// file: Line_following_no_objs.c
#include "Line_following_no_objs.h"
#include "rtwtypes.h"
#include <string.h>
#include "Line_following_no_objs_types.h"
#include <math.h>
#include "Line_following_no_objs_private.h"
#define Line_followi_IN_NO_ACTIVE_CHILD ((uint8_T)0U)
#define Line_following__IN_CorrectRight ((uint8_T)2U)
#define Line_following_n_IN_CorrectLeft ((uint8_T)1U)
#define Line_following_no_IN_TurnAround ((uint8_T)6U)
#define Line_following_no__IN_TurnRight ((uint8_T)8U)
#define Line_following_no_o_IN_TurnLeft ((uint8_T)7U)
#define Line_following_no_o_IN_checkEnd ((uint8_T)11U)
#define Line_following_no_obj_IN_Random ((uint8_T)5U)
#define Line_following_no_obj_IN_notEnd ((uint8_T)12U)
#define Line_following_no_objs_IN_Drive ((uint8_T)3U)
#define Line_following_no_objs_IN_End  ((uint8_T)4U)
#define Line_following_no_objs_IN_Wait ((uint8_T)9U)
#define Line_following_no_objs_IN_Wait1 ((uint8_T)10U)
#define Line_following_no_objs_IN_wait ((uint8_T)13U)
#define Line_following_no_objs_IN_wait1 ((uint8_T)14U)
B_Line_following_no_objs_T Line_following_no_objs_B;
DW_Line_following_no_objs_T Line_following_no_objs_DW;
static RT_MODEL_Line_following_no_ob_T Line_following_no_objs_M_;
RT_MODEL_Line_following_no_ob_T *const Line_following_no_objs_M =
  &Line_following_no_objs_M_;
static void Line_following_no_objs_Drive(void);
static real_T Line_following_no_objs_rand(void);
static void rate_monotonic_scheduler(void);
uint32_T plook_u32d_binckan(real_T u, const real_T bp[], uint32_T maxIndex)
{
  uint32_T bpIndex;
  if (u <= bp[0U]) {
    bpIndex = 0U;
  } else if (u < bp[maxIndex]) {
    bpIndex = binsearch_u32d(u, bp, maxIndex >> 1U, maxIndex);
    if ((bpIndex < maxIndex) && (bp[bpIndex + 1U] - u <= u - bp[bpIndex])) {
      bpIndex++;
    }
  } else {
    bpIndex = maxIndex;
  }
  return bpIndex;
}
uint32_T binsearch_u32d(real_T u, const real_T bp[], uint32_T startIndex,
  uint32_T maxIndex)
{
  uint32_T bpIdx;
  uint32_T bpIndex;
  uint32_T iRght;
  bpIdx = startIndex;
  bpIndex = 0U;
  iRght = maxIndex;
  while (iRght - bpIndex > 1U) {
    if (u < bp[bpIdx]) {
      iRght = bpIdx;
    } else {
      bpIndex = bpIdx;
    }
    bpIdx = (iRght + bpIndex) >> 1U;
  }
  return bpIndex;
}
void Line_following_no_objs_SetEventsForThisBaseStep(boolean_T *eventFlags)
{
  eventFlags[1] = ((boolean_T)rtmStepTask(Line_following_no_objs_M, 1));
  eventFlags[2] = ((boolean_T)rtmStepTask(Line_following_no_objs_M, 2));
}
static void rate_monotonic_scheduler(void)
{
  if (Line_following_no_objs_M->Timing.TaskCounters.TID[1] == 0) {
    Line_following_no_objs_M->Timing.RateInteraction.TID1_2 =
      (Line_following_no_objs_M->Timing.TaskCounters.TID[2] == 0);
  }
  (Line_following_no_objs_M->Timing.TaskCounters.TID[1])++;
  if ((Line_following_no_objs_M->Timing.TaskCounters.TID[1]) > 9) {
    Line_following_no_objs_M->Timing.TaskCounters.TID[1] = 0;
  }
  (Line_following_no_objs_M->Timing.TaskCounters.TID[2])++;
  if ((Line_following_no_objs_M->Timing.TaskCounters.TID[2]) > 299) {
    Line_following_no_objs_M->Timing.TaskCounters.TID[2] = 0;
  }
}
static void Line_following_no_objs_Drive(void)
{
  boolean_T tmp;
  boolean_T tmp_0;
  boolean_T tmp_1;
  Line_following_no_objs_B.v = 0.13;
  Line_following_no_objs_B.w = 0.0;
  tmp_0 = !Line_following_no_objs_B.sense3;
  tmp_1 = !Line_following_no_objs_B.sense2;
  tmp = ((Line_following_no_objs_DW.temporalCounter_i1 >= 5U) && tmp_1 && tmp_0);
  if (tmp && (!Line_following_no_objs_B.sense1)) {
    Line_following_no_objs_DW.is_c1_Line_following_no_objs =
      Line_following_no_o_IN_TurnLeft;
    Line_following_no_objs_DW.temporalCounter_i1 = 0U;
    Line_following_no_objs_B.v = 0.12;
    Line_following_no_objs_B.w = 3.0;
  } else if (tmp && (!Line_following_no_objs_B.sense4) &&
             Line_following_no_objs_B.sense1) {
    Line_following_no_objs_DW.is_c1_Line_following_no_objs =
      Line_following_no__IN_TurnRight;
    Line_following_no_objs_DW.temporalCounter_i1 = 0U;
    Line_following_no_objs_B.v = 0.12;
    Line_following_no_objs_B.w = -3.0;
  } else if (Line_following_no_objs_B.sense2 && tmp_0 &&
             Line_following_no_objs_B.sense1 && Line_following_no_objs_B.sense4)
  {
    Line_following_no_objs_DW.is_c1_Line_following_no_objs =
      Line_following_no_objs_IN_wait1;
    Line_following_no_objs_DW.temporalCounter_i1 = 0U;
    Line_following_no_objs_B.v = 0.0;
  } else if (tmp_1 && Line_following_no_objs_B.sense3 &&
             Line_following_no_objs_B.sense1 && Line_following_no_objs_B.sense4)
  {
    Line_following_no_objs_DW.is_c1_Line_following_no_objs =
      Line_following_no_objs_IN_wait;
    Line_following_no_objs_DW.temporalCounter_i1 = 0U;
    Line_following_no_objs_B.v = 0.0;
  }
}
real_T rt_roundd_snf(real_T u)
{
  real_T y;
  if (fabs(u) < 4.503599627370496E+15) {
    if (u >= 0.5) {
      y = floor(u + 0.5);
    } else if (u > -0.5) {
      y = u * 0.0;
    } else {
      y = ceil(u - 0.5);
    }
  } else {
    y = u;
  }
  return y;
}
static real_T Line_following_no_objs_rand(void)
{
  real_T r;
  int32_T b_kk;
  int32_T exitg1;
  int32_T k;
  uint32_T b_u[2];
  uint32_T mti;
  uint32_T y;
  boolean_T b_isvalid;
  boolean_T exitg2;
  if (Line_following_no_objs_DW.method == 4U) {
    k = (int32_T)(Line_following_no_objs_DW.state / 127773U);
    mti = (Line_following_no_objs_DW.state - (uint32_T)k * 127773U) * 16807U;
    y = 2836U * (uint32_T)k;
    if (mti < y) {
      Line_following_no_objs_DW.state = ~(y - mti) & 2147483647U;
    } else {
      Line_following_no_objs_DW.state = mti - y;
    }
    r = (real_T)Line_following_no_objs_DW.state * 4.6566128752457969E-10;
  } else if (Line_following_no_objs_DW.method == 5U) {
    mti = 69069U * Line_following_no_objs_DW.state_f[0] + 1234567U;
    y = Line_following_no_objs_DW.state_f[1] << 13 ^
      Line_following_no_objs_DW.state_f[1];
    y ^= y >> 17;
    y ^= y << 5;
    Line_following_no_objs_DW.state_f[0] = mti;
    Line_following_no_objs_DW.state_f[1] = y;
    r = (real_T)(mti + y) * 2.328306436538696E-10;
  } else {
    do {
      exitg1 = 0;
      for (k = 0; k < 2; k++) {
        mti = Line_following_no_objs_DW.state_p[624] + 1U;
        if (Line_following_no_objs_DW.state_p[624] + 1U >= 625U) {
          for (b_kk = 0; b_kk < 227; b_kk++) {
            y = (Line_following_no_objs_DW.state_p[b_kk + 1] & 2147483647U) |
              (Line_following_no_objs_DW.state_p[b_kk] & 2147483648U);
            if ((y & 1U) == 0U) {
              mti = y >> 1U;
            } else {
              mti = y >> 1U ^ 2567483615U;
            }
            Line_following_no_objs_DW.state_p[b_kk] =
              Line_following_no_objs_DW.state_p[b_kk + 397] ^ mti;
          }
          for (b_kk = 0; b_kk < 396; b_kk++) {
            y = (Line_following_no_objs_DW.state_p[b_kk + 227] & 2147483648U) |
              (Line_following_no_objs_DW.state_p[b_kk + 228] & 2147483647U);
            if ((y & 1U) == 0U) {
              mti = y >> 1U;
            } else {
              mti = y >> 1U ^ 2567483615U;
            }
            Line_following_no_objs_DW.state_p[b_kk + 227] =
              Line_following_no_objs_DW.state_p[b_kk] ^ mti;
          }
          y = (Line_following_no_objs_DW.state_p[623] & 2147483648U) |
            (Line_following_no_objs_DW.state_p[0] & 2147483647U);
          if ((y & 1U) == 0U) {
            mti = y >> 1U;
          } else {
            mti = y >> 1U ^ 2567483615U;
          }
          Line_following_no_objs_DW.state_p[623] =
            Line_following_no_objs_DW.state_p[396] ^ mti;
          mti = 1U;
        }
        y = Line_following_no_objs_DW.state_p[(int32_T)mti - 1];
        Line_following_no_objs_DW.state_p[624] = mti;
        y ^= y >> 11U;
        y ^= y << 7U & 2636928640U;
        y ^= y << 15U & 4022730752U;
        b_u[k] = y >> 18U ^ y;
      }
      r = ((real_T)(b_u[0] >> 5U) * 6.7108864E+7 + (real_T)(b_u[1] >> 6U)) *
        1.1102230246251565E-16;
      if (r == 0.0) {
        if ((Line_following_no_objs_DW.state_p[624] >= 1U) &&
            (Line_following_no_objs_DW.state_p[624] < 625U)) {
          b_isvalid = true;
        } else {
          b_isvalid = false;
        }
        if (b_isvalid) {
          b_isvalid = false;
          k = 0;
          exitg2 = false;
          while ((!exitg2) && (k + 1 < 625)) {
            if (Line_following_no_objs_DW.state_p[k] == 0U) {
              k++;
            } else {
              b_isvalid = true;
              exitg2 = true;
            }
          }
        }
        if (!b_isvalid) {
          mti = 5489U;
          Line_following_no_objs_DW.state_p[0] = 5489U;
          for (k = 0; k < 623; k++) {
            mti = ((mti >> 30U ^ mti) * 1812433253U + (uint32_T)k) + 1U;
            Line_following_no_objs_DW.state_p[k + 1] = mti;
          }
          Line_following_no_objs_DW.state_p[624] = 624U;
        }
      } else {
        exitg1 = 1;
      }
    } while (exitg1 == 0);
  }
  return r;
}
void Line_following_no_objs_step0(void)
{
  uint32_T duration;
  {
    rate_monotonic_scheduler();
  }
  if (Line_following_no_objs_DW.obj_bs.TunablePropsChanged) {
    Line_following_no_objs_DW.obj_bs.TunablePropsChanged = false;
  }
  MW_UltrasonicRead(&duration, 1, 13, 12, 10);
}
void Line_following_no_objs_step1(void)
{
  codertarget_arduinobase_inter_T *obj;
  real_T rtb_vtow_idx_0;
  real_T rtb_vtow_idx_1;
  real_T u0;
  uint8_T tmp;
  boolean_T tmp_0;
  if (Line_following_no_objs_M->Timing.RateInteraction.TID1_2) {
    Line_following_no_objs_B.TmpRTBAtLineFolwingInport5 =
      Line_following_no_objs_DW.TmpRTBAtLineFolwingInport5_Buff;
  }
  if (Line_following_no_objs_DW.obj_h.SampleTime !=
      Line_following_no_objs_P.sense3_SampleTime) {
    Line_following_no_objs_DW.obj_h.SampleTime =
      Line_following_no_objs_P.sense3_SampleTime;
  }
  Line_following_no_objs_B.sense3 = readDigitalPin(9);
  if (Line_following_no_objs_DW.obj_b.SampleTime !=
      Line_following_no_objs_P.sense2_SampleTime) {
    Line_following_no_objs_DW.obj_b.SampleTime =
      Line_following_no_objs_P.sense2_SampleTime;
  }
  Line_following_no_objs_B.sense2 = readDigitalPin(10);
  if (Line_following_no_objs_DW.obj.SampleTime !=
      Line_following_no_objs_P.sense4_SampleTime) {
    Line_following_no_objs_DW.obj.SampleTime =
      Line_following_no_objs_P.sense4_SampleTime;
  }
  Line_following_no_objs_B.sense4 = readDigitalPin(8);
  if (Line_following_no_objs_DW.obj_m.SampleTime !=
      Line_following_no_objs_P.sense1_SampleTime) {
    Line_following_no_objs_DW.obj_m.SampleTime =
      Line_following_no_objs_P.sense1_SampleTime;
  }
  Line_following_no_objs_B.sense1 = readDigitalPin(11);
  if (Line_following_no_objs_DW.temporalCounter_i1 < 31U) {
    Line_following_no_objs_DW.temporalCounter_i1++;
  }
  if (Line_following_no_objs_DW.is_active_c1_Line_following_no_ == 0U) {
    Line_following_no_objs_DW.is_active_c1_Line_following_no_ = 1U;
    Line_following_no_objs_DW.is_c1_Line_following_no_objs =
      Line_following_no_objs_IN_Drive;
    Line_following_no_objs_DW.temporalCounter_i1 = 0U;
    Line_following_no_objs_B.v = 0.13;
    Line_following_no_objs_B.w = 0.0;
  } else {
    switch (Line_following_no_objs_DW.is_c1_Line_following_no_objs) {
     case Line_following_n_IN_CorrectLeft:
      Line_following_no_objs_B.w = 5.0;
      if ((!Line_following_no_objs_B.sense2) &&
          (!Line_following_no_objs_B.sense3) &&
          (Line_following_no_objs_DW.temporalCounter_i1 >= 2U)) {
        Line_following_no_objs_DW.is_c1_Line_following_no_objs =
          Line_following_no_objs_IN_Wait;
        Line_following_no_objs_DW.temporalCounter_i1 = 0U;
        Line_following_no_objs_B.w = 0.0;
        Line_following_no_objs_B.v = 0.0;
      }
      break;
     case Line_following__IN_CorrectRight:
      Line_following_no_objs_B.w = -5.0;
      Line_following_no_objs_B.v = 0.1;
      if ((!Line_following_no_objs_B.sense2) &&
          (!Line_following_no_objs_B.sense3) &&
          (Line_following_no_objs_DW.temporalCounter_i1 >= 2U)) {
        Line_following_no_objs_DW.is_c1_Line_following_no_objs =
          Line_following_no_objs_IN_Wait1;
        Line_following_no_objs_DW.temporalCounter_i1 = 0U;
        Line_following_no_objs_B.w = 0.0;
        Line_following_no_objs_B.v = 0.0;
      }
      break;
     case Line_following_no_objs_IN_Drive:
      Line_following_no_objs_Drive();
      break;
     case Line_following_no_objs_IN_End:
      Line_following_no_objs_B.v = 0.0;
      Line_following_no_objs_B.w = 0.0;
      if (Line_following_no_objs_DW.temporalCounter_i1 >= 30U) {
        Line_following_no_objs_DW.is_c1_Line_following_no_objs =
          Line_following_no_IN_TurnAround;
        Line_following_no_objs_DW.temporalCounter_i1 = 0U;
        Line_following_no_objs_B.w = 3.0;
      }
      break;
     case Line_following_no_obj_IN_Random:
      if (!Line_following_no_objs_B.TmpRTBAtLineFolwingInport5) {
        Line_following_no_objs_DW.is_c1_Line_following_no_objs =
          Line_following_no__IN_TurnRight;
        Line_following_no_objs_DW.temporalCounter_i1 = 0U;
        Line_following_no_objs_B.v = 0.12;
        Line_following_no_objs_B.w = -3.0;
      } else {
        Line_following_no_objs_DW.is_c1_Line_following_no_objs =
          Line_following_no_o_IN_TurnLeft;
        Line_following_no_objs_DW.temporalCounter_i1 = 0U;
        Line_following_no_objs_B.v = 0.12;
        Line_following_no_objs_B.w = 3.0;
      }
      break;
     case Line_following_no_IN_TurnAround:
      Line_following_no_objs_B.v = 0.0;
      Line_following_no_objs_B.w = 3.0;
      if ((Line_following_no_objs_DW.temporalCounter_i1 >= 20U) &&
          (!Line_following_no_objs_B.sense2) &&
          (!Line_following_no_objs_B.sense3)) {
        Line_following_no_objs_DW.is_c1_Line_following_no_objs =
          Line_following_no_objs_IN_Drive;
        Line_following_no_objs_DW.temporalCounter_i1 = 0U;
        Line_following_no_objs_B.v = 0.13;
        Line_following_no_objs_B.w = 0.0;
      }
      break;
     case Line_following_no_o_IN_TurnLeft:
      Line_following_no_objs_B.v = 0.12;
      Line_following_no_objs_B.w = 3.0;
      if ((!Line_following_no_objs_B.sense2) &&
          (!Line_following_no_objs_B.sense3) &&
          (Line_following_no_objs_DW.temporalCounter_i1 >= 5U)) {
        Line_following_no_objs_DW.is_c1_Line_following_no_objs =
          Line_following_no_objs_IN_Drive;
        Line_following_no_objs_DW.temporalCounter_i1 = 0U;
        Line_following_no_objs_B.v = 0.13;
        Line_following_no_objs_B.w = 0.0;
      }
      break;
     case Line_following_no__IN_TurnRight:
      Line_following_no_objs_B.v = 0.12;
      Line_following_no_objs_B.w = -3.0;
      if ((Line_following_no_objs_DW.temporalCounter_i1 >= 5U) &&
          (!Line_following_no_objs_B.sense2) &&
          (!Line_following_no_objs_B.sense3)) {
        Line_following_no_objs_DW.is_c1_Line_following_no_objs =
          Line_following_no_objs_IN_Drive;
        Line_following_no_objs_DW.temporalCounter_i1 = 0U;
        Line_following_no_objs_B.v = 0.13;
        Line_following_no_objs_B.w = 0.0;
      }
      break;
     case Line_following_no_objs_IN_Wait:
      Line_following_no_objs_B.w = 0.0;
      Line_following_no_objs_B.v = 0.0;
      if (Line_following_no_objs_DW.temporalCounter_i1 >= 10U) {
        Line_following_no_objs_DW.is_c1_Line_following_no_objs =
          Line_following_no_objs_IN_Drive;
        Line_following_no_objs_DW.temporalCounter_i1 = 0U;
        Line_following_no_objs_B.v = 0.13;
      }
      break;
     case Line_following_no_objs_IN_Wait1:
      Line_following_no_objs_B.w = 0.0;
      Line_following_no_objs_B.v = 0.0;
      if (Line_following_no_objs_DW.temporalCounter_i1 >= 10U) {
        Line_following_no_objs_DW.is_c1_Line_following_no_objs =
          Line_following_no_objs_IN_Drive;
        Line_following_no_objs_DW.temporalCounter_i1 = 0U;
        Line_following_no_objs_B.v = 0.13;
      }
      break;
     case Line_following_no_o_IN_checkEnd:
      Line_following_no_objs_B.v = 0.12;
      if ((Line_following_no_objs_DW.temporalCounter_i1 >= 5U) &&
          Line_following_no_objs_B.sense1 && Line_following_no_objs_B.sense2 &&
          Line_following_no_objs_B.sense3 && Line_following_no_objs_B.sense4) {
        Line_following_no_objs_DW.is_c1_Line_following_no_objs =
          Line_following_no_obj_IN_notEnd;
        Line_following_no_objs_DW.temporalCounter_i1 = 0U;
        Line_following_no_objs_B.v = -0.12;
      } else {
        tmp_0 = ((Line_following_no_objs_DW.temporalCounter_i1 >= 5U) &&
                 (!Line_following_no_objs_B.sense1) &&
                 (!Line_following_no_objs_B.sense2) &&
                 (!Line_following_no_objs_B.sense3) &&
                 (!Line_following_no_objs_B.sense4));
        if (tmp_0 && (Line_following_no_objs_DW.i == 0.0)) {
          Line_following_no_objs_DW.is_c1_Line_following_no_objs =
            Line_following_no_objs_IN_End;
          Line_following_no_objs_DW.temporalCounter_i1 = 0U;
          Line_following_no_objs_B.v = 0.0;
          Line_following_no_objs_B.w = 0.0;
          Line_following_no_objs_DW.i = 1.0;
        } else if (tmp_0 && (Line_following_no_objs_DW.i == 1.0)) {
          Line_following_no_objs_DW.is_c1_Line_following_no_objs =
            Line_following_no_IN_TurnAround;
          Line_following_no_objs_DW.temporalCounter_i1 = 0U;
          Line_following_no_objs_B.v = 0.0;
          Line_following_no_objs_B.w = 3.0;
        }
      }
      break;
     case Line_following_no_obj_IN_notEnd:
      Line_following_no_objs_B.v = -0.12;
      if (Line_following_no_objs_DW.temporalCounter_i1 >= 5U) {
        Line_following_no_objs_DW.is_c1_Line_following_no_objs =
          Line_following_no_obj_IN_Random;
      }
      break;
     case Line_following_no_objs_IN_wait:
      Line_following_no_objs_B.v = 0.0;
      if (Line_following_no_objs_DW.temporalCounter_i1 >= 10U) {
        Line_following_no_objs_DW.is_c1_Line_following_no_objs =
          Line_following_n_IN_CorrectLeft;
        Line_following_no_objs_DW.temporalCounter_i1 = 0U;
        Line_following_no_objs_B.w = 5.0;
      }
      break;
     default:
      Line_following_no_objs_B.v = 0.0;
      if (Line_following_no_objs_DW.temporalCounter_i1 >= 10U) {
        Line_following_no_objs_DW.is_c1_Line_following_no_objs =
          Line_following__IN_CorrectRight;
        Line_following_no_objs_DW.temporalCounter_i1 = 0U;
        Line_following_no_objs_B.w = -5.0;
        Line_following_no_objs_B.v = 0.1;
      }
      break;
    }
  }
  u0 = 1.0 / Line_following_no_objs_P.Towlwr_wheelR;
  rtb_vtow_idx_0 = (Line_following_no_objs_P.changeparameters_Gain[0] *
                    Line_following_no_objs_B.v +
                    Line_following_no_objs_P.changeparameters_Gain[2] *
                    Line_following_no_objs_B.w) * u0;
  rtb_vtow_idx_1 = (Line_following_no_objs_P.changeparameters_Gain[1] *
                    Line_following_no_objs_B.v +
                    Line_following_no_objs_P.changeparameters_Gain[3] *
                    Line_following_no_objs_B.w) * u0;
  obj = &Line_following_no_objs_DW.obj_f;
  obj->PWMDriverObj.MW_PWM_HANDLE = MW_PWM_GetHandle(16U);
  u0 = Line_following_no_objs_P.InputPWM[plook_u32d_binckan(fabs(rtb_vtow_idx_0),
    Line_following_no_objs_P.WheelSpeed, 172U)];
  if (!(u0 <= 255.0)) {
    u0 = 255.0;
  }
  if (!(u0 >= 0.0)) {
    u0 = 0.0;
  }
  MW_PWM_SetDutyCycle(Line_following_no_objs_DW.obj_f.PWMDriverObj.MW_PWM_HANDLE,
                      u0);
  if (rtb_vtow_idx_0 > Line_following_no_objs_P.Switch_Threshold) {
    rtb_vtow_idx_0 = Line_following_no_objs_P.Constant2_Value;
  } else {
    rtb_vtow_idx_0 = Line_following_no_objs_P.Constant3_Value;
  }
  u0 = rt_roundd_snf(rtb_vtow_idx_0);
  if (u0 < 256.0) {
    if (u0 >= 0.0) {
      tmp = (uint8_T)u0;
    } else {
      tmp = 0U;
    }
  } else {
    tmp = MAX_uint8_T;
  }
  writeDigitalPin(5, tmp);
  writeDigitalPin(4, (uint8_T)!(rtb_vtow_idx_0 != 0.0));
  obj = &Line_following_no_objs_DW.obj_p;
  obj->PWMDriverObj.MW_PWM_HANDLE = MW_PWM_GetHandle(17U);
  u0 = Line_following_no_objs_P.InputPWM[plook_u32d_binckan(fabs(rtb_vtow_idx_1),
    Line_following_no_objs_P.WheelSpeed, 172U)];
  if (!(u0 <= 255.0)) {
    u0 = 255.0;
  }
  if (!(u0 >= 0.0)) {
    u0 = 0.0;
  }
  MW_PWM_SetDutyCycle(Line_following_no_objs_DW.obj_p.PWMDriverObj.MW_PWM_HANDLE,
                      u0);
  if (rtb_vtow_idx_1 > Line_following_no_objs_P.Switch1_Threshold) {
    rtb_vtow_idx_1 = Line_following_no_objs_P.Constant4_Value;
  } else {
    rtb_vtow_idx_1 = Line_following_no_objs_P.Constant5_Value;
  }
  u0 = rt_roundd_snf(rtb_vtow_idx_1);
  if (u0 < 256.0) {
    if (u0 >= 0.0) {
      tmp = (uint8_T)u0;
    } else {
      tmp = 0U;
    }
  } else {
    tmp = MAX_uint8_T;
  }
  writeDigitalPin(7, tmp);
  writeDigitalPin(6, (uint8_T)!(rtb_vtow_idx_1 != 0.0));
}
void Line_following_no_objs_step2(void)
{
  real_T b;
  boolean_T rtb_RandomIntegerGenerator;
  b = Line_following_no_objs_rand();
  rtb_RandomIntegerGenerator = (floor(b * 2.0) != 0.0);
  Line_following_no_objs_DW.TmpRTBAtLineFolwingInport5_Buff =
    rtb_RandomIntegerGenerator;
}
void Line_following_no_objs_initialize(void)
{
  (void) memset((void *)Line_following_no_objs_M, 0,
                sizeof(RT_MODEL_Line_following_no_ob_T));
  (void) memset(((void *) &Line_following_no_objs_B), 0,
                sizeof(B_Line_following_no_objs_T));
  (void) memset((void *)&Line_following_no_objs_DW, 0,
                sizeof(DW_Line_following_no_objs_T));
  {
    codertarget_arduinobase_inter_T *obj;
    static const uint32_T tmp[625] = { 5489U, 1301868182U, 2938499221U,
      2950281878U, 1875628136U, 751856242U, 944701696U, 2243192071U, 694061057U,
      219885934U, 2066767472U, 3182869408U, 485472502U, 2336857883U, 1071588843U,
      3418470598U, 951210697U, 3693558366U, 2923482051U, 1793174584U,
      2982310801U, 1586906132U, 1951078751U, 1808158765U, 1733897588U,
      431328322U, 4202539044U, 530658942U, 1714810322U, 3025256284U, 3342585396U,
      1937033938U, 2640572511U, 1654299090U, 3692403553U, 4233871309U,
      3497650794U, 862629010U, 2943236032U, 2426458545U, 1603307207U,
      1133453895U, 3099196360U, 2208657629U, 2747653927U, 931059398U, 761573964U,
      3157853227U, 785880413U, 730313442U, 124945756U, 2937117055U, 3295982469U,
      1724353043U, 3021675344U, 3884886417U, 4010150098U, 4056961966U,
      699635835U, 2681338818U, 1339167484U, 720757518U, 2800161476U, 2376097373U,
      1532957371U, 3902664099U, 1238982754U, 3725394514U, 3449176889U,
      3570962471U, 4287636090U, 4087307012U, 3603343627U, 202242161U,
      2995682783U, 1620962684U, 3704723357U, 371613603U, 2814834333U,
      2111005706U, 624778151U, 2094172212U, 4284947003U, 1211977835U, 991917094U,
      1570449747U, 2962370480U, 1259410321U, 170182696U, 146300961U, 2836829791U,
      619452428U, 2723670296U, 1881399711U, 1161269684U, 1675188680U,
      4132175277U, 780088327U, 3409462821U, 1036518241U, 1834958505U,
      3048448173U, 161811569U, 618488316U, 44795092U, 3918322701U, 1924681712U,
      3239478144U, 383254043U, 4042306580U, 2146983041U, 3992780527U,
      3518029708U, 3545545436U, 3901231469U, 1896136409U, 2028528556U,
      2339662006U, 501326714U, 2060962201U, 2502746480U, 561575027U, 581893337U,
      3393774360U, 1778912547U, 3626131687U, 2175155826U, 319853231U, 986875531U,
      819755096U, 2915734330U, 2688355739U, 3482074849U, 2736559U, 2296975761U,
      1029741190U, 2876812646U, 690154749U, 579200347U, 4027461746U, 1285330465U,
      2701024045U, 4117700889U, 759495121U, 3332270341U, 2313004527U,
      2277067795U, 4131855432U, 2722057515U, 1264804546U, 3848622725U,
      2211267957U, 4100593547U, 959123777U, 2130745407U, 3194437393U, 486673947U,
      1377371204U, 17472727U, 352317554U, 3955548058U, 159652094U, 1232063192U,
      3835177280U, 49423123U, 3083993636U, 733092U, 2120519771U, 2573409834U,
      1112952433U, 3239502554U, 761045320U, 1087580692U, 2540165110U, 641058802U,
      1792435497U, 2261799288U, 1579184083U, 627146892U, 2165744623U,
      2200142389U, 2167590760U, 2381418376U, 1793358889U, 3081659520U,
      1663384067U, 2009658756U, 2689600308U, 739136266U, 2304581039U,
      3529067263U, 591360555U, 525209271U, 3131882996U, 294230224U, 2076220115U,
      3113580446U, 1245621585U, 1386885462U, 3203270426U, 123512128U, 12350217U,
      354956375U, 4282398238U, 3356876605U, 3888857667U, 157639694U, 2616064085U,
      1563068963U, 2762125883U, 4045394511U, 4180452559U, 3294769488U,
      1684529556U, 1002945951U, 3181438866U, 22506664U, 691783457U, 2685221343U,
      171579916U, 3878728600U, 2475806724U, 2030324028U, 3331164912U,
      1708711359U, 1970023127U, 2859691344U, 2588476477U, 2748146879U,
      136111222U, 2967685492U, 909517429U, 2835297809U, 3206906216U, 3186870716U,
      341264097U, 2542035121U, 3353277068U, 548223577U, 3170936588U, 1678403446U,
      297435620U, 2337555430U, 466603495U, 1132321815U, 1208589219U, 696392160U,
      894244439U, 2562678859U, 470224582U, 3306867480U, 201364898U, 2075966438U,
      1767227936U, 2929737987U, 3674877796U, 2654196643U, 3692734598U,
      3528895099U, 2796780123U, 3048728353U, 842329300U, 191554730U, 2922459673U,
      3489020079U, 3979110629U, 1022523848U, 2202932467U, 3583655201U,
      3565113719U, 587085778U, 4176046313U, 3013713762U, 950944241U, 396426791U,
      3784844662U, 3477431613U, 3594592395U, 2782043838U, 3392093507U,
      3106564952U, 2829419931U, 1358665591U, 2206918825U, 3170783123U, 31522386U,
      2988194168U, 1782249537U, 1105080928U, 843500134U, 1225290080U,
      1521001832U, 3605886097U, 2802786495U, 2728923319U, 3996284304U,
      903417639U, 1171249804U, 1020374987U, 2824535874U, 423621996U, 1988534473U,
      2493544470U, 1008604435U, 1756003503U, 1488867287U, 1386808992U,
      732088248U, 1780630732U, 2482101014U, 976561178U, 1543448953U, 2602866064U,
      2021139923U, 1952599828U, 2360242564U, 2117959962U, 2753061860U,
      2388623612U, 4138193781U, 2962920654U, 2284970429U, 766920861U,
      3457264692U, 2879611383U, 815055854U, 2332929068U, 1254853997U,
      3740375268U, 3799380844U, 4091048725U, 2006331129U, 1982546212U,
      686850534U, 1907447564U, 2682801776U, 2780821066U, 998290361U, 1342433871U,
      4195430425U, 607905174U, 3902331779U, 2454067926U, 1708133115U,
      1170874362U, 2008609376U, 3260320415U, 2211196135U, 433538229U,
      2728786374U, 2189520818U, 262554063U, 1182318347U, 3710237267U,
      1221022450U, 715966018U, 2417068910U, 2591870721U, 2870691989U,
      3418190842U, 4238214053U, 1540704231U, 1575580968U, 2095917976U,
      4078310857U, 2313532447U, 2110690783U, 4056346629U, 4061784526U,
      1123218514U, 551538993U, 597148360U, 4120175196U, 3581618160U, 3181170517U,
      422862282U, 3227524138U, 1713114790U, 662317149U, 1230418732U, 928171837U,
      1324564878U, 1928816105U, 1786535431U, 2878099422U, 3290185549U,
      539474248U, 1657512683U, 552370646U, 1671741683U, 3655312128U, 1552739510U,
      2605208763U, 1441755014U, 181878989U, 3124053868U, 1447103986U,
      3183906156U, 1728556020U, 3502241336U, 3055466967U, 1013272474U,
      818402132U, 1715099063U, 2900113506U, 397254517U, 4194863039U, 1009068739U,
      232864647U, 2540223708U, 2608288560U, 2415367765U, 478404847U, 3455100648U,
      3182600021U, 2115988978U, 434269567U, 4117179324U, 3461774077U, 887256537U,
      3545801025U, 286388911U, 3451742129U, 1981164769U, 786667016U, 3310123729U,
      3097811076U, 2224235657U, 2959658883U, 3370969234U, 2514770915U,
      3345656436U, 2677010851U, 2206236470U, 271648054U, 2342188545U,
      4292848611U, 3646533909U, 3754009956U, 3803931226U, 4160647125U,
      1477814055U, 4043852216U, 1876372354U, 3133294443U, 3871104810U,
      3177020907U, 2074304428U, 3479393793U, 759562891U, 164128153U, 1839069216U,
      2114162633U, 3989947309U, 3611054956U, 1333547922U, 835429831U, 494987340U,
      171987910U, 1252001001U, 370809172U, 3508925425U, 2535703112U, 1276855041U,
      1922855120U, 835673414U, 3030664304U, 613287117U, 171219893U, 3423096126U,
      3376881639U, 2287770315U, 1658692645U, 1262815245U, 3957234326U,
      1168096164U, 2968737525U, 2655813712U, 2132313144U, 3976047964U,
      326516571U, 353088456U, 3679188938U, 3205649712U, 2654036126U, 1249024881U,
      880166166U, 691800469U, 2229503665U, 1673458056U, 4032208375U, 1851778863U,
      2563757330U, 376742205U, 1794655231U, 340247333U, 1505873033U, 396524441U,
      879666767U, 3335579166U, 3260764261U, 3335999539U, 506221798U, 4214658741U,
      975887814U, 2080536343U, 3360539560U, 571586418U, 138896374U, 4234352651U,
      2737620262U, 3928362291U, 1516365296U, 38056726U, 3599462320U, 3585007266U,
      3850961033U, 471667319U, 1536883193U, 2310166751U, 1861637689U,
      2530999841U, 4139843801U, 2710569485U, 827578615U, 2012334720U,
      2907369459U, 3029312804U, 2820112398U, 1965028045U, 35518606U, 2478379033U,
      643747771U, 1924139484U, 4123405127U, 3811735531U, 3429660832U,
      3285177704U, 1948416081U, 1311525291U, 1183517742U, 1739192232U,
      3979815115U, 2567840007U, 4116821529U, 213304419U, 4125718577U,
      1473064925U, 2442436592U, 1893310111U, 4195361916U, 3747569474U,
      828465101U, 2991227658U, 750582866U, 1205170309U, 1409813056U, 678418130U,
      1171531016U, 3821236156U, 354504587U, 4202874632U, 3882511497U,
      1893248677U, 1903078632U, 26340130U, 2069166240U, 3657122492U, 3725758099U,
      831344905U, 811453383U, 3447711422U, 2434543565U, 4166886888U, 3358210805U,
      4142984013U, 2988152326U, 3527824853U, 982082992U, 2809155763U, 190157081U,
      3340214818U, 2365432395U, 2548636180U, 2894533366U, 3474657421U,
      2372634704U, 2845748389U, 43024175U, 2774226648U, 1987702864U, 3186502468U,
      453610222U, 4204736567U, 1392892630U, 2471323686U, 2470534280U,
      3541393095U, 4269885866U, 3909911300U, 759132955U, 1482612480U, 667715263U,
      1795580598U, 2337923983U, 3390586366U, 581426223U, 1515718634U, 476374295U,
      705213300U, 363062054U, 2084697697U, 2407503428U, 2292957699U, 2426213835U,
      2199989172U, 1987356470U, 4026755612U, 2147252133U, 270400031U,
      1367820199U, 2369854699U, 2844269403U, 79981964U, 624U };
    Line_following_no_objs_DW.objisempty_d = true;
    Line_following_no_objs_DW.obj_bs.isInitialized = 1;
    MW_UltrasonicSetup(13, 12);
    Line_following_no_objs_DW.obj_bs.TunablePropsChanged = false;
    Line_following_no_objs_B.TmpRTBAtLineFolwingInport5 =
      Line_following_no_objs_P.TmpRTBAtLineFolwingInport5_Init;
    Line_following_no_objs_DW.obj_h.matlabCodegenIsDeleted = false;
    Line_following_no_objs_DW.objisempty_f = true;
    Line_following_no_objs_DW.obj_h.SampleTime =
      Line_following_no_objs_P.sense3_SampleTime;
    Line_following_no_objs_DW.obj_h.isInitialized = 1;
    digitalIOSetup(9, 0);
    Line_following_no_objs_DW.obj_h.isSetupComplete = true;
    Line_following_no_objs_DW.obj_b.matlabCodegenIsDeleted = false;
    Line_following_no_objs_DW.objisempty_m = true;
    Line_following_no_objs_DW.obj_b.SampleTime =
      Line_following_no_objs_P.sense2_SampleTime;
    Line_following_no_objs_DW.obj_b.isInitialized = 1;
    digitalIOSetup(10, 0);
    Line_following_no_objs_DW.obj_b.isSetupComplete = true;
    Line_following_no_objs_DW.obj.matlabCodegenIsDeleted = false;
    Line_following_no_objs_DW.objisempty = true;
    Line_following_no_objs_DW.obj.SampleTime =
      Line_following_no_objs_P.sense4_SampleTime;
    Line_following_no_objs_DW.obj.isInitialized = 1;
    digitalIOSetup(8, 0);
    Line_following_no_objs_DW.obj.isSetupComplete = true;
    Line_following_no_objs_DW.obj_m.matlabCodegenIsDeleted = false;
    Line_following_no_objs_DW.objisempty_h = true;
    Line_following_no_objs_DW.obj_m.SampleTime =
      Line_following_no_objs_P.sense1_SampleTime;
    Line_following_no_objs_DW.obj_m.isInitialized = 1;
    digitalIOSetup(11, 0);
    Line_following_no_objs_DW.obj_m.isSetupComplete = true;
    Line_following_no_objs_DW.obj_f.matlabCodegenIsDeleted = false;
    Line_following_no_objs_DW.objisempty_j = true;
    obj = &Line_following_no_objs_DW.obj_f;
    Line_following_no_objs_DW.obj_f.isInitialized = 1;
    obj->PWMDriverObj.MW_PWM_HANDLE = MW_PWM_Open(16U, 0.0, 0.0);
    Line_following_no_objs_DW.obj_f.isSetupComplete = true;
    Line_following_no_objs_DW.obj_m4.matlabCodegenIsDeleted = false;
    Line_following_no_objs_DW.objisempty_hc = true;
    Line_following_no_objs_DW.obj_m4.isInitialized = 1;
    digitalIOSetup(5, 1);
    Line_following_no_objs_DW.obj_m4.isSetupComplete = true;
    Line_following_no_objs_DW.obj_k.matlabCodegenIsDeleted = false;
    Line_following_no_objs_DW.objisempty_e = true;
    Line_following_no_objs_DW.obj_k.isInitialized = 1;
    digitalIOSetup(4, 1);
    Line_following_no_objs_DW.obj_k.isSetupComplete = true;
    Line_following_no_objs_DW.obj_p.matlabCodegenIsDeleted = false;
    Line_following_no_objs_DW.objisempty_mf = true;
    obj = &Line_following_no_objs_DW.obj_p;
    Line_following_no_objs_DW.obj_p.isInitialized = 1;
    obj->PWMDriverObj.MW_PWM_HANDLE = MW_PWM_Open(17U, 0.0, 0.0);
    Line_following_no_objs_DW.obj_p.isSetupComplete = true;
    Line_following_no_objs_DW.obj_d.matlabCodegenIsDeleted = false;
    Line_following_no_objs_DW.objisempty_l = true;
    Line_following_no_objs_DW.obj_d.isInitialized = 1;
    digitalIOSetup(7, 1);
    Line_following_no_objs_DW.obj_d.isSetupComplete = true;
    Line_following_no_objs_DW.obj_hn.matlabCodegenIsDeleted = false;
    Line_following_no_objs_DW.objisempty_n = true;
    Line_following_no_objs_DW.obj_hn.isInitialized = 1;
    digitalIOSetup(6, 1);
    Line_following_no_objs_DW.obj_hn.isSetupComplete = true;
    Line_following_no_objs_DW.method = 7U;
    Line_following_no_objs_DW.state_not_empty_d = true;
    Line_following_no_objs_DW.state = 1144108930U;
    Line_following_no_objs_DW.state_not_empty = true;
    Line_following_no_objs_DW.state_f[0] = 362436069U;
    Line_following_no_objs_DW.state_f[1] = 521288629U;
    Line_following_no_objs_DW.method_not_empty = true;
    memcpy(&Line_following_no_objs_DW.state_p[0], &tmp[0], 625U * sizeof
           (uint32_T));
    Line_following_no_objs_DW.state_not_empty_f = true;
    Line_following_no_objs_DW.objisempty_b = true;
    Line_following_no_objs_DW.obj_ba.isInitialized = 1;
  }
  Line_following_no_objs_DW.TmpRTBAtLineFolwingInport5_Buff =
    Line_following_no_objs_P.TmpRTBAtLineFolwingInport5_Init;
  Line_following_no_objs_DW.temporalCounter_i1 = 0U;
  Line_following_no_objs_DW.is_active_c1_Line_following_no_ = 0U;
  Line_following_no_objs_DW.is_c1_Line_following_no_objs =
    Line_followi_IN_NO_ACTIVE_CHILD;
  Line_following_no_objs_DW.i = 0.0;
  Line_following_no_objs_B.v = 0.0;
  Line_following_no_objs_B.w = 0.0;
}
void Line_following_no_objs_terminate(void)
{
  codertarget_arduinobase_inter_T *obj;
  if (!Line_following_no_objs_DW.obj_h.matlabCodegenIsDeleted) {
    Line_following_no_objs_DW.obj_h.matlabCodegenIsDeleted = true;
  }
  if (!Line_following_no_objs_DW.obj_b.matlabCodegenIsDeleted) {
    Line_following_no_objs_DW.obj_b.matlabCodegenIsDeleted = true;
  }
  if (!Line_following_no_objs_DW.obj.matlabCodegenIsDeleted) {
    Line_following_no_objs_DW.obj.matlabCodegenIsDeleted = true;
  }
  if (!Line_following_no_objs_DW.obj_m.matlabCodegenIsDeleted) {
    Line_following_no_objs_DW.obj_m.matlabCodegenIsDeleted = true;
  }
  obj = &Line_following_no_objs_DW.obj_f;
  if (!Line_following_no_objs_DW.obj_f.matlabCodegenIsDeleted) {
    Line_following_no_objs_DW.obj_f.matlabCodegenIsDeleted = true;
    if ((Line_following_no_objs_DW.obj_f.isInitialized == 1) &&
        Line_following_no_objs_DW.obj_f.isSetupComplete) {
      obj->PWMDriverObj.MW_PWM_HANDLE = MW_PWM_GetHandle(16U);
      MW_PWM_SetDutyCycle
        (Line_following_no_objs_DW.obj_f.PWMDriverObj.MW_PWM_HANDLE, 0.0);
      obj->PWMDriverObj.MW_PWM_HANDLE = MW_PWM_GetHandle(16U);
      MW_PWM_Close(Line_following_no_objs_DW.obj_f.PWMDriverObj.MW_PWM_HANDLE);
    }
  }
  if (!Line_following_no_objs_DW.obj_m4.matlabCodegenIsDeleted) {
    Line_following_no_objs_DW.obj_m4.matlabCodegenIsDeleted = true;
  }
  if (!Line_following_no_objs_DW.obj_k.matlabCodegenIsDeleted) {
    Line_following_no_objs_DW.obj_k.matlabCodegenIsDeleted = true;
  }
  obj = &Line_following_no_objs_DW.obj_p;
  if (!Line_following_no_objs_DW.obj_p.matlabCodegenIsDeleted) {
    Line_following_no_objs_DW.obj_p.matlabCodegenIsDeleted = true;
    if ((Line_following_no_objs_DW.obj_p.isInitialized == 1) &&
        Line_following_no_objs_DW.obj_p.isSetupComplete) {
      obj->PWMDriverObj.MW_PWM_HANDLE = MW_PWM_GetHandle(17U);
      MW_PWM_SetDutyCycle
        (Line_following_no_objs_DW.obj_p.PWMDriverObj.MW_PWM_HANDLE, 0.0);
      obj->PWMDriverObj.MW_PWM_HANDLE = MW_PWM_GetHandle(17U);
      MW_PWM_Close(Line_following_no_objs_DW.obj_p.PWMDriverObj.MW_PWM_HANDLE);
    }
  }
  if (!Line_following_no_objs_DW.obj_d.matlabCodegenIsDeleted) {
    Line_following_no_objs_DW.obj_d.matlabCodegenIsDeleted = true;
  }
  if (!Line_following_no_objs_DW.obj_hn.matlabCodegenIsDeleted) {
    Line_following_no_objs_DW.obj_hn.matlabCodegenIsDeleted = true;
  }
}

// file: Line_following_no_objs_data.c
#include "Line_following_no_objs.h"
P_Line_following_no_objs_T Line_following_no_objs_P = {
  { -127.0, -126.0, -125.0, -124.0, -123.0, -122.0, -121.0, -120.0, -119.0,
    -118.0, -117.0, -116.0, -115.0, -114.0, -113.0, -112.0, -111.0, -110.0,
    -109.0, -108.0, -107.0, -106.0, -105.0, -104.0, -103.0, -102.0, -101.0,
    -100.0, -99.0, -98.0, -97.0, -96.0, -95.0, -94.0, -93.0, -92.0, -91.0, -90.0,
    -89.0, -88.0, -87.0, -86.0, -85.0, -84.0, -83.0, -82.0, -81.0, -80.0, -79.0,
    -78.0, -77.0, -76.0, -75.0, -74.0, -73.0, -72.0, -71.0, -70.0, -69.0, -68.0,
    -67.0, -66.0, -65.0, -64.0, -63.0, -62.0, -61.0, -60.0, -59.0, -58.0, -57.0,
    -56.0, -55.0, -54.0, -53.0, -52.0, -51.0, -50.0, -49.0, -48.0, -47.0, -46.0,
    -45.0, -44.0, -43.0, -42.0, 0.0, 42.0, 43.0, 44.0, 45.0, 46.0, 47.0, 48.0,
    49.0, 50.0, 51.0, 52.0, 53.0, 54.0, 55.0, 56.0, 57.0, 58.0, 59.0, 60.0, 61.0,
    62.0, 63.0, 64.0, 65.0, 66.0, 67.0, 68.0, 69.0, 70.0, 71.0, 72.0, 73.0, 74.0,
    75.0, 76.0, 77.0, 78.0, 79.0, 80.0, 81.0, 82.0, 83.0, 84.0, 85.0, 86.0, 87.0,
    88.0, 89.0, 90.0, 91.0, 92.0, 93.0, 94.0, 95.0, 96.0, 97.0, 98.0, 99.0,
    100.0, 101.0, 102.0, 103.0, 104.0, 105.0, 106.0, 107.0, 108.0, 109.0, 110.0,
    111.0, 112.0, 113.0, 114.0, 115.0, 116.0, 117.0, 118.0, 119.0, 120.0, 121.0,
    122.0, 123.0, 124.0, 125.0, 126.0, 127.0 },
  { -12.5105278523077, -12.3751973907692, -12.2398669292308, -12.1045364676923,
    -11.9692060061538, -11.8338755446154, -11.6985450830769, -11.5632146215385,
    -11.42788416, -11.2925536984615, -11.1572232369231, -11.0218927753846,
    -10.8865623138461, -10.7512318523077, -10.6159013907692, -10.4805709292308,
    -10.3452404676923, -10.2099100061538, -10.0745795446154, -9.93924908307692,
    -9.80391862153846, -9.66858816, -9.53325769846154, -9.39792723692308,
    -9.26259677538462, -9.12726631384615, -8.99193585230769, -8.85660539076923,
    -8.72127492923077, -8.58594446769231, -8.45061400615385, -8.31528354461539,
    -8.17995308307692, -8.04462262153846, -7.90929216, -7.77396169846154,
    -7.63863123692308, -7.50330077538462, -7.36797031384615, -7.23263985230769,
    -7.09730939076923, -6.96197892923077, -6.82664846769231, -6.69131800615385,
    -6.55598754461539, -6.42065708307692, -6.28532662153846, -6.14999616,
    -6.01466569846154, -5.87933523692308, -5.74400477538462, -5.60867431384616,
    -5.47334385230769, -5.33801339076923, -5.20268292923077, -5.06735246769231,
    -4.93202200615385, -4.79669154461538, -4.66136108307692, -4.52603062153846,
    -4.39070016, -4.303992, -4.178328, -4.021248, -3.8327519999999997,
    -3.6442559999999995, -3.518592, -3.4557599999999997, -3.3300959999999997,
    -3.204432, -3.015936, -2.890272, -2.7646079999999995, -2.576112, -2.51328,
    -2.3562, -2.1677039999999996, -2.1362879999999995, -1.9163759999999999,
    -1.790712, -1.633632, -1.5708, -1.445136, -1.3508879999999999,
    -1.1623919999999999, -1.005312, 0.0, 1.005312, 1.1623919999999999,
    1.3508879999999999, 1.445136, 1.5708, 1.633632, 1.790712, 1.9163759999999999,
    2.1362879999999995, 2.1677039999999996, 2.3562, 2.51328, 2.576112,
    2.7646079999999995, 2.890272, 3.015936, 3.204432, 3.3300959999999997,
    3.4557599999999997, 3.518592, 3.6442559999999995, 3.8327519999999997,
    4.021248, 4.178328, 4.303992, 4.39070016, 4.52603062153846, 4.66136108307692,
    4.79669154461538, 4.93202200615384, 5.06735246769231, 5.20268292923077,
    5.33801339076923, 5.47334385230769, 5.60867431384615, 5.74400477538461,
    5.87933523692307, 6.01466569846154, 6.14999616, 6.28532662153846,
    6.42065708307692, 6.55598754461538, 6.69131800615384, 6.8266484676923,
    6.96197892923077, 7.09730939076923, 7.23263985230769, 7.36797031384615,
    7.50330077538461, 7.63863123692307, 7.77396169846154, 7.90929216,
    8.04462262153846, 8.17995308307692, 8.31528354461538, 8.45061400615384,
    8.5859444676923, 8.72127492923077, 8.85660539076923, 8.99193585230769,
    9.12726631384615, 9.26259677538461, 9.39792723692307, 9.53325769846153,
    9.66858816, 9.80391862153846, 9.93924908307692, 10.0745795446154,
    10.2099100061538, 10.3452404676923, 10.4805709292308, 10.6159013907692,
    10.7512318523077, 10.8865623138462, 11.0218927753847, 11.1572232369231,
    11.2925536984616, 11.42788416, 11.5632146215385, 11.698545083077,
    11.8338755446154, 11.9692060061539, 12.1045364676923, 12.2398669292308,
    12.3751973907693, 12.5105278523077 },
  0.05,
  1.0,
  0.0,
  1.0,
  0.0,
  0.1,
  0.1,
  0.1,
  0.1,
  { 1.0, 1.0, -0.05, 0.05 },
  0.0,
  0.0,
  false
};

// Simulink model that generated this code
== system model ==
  UltrasonicSensor#1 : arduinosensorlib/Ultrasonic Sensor
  PWM#1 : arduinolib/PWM  pinNumber=16  <- 1: Lookup_nD#1
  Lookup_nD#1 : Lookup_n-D  BreakpointsForDimension1=WheelSpeed  Table=InputPWM  InterpMethod=Nearest  <- 1: Abs#1
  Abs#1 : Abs  <- 1: Towlwr
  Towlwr : mobileRoboticsTrainingLib/To wlwr  <- 1: Stateflowchart#1, 2: Stateflowchart#1/2
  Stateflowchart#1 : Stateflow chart  <- 1: sense3, 2: sense2, 3: sense4, 4: sense1, 5: RandomIntegerGenerator
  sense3 : arduinolib/Digital Input  pinNumber=9
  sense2 : arduinolib/Digital Input  pinNumber=10
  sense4 : arduinolib/Digital Input  pinNumber=8
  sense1 : arduinolib/Digital Input  pinNumber=11
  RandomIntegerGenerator : commrandsrc3/Random Integer Generator
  DigitalOutput#1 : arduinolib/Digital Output  pinNumber=5  <- 1: Switch
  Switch : Switch  Criteria=u2 > Threshold  <- 1: Constant2, 2: Towlwr, 3: Constant3
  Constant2 : Constant
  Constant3 : Constant  Value=0
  DigitalOutput#2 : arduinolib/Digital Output  pinNumber=4  <- 1: Logic#1
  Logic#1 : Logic  Operator=NOT  <- 1: Switch
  PWM#2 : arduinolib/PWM  pinNumber=17  <- 1: Lookup_nD#2
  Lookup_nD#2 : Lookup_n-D  BreakpointsForDimension1=WheelSpeed  Table=InputPWM  InterpMethod=Nearest  <- 1: Abs#2
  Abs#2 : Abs  <- 1: Towlwr/2
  DigitalOutput#3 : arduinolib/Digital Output  pinNumber=7  <- 1: Switch1
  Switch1 : Switch  Criteria=u2 > Threshold  <- 1: Constant4, 2: Towlwr/2, 3: Constant5
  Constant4 : Constant
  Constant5 : Constant  Value=0
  DigitalOutput#4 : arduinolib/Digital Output  pinNumber=6  <- 1: Logic#2
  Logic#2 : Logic  Operator=NOT  <- 1: Switch1
== stateflow chart Stateflowchart#1 ==
  state Random
    entry:
    dir;
  state notEnd
    entry:
    v=-0.12;
  state End
    entry:
    v=0;
    w=0;
    i=1;
  state TurnAround
    entry:
    v=0;
    w=3;
  state checkEnd
    entry:
    v=0.12;
  state TurnLeft
    entry:
    v=0.12;
    w=3;
  state TurnRight
    entry:
    v=0.12;
    w=-3;
  state Drive
    entry:
    v=0.13;
    w=0;
    i;
    n;
    data1;
  state Wait1
    entry:
    w=0;
    v=0;
  state CorrectRight
    entry:
    w=-5;
    v=0.1;
  state CorrectLeft
    entry:
    w=5;
  state Wait
    entry:
    w=0;
    v=0;
  state wait
    entry:
    v=0;
  state wait1
    entry:
    v=0;
  checkEnd -> TurnAround [order 3] : [after(0.5,sec) &&sense1 ==0 && sense2 == 0 && sense3 ==0 && sense4==0 && i==1]
  Random -> TurnLeft [order 2] : [dir==1]
  Random -> TurnRight [order 1] : [dir==0]
  notEnd -> Random : [after(0.5,sec)]
  checkEnd -> notEnd [order 1] : [after(0.5,sec) &&sense1 == 1 && sense2 == 1 && sense3 ==1 && sense4==1 ]
  End -> TurnAround : [after(3,sec)]
  checkEnd -> End [order 2] : [after(0.5,sec) &&sense1 ==0 && sense2 == 0 && sense3 ==0 && sense4==0 && i==0]
  TurnAround -> Drive : [after(2,sec) && sense2 == 0 && sense3 == 0]
  TurnRight -> Drive : [after(0.5,sec) && sense2 ==0 && sense3 ==0]
  Drive -> TurnLeft [order 1] : [after(0.5,sec) && sense2 == 0 && sense3 == 0 && sense1 == 0 ]
  (default) -> Drive
  Drive -> TurnRight [order 2] : [after(0.5,sec) && sense2 == 0 && sense3 == 0 && sense4 == 0 && sense1==1]
  TurnLeft -> Drive : [sense2==0 && sense3==0 && after(0.5,sec)]
  Wait1 -> Drive : [after(1,sec)]
  CorrectRight -> Wait1 : [sense2==0 && sense3 == 0 && after(0.2,sec)]
  wait1 -> CorrectRight : [after(1,sec)]
  CorrectLeft -> Wait : [sense2 ==0 && sense3 ==0&& after(0.2,sec)]
  Wait -> Drive : [after(1,sec)]
  Drive -> wait [order 4] : [sense2==0 && sense3 ==1 && sense1 == 1 &&sense4 ==1]
  Drive -> wait1 [order 3] : [sense2==1 && sense3 ==0 && sense1 == 1 &&sense4 ==1]
  wait -> CorrectLeft : [after(1,sec)]
  data: v output; w output; sense3 input; sense2 input; sense4 input; sense1 input; i local =0; dir input; n local =1; data1 local =100
